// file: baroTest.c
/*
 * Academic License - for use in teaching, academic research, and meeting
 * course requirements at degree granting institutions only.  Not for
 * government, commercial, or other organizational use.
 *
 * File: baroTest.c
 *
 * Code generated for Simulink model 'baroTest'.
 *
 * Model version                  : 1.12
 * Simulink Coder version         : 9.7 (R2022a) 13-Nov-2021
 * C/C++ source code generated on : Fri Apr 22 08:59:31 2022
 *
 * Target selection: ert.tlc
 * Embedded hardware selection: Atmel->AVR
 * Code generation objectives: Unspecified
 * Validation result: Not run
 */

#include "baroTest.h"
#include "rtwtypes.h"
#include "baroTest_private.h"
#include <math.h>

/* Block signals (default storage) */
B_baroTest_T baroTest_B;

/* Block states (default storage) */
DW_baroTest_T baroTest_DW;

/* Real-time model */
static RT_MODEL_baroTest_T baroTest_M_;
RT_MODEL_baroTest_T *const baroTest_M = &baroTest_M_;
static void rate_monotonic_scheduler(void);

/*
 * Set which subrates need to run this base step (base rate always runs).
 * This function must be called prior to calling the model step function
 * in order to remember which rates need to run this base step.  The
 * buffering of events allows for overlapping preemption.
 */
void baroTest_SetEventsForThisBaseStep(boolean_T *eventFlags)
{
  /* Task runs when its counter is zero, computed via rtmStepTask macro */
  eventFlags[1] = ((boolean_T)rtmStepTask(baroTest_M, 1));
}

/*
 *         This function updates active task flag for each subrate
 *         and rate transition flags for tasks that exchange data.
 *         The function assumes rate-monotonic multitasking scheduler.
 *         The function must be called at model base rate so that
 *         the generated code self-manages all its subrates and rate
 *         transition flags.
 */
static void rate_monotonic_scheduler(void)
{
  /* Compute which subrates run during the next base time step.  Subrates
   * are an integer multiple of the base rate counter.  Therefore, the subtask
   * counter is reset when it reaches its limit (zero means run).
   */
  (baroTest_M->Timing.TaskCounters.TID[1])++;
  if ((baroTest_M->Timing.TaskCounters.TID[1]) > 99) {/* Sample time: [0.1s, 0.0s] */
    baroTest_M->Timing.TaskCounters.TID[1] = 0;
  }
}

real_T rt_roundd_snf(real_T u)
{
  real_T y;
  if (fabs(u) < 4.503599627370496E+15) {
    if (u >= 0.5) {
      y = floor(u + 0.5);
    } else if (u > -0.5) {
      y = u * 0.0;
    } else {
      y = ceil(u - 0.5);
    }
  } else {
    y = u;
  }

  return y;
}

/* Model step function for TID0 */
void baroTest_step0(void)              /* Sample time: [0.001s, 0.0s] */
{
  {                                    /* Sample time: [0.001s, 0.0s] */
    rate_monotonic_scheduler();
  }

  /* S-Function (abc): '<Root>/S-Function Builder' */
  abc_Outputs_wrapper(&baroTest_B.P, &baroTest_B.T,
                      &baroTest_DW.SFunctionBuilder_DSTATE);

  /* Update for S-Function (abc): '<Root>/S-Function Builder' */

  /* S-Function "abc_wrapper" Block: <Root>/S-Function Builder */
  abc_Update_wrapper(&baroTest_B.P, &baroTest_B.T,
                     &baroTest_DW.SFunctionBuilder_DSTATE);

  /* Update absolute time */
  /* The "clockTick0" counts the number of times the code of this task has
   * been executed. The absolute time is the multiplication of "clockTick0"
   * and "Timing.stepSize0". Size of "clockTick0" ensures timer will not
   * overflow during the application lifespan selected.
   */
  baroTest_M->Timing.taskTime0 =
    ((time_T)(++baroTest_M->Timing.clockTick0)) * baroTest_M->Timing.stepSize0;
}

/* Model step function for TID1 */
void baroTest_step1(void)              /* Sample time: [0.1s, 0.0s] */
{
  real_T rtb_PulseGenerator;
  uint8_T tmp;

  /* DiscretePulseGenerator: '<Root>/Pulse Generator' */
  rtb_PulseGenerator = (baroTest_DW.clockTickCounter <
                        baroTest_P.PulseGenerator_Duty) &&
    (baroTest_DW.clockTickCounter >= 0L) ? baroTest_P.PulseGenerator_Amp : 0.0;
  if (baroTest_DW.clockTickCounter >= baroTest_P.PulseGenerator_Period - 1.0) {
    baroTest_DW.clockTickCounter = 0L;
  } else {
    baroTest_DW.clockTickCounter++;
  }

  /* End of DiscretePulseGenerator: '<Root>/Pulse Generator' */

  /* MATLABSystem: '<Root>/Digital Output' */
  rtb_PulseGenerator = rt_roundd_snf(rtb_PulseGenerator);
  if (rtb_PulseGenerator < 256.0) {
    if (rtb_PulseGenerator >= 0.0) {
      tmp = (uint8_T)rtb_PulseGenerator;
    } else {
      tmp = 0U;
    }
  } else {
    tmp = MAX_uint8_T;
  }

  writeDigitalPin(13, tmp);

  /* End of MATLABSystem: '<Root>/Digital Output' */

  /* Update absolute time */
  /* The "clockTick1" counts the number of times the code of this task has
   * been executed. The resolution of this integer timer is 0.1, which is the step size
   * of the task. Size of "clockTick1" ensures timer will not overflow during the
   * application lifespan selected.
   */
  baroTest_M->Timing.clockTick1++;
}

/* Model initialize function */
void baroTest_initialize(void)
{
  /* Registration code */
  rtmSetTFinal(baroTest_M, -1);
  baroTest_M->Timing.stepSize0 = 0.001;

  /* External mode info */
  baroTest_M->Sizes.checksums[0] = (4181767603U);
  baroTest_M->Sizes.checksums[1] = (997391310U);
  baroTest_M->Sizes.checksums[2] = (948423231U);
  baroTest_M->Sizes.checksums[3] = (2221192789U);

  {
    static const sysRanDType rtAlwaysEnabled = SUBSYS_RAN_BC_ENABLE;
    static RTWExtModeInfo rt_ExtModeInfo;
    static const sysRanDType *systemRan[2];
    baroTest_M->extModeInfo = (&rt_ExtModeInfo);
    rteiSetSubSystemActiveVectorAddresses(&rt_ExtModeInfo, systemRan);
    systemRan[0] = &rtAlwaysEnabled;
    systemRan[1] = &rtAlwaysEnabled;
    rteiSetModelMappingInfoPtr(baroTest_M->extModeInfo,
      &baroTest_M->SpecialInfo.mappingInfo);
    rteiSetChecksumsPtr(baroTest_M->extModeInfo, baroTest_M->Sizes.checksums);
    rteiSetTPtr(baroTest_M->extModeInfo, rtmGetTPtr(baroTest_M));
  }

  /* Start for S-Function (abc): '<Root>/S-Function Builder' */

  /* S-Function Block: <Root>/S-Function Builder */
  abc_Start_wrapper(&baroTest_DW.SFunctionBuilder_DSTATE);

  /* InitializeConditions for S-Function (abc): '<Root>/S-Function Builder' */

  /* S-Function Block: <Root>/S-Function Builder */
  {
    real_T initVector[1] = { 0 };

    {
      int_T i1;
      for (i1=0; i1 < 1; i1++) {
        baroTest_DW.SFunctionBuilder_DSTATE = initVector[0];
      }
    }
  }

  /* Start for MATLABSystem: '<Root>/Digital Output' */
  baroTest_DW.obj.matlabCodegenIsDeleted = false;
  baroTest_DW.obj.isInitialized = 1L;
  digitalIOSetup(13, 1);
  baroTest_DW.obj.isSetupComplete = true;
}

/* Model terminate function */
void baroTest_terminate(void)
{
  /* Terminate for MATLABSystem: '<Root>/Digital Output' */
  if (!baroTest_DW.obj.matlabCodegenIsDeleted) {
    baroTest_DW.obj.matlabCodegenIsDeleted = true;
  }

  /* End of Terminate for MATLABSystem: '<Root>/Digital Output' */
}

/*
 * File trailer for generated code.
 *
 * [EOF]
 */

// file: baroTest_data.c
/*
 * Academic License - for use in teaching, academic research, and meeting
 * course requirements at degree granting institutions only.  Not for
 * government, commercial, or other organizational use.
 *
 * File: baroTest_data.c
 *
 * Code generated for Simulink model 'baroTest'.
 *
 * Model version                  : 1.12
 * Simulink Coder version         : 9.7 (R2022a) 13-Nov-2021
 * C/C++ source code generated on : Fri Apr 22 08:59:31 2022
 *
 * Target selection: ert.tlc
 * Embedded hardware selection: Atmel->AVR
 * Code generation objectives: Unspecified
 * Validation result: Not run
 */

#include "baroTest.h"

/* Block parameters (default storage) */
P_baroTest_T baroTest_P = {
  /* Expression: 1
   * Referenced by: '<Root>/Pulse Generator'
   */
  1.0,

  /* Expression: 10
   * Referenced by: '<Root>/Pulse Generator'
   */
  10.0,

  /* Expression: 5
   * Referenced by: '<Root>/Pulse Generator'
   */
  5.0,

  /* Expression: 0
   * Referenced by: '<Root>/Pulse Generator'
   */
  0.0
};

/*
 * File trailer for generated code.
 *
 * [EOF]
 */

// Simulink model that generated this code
simulink model "baroTest"  (R2022a)
settings: Solver=FixedStepAuto  StartTime=0.0  StopTime=inf  RelTol=1e-3  EnableMultiTasking=on
libraries: arduinolib x1

== system baroTest ==
  Digital Output : arduinolib/Digital Output  pinNumber=13  Direction=output  blockPlatform=arduino
  Pulse Generator : DiscretePulseGenerator  Period=10  PulseWidth=5  SampleTime=0.1
  S-Function Builder : S-Function  FunctionName=abc  SFunctionModules=abc_wrapper  SFunctionDeploymentMode=off  EnableBusSupport=off  mask(S-Function Builder){}
      mask help: Simulink:masks:SFunctionBuilder_MD
      mask init:
      | val = [[.9  0.75 0.75 1 1 .9 .9 1]',[1 1 0.75 0.75 .9 .9 1 .9]'];try , sys = get_param(gcb,'SfunBuilderFcnName');if isempty(sys), sys = get_param(gcb,'FunctionName'); end,catch, sys = get_param(gcb,'FunctionName'); end
  Scope : Scope
  Scope1 : Scope
  wires:
  S-Function Builder/1 -> Scope/1
  Pulse Generator/1 -> Digital Output/1
  S-Function Builder/2 -> Scope1/1
